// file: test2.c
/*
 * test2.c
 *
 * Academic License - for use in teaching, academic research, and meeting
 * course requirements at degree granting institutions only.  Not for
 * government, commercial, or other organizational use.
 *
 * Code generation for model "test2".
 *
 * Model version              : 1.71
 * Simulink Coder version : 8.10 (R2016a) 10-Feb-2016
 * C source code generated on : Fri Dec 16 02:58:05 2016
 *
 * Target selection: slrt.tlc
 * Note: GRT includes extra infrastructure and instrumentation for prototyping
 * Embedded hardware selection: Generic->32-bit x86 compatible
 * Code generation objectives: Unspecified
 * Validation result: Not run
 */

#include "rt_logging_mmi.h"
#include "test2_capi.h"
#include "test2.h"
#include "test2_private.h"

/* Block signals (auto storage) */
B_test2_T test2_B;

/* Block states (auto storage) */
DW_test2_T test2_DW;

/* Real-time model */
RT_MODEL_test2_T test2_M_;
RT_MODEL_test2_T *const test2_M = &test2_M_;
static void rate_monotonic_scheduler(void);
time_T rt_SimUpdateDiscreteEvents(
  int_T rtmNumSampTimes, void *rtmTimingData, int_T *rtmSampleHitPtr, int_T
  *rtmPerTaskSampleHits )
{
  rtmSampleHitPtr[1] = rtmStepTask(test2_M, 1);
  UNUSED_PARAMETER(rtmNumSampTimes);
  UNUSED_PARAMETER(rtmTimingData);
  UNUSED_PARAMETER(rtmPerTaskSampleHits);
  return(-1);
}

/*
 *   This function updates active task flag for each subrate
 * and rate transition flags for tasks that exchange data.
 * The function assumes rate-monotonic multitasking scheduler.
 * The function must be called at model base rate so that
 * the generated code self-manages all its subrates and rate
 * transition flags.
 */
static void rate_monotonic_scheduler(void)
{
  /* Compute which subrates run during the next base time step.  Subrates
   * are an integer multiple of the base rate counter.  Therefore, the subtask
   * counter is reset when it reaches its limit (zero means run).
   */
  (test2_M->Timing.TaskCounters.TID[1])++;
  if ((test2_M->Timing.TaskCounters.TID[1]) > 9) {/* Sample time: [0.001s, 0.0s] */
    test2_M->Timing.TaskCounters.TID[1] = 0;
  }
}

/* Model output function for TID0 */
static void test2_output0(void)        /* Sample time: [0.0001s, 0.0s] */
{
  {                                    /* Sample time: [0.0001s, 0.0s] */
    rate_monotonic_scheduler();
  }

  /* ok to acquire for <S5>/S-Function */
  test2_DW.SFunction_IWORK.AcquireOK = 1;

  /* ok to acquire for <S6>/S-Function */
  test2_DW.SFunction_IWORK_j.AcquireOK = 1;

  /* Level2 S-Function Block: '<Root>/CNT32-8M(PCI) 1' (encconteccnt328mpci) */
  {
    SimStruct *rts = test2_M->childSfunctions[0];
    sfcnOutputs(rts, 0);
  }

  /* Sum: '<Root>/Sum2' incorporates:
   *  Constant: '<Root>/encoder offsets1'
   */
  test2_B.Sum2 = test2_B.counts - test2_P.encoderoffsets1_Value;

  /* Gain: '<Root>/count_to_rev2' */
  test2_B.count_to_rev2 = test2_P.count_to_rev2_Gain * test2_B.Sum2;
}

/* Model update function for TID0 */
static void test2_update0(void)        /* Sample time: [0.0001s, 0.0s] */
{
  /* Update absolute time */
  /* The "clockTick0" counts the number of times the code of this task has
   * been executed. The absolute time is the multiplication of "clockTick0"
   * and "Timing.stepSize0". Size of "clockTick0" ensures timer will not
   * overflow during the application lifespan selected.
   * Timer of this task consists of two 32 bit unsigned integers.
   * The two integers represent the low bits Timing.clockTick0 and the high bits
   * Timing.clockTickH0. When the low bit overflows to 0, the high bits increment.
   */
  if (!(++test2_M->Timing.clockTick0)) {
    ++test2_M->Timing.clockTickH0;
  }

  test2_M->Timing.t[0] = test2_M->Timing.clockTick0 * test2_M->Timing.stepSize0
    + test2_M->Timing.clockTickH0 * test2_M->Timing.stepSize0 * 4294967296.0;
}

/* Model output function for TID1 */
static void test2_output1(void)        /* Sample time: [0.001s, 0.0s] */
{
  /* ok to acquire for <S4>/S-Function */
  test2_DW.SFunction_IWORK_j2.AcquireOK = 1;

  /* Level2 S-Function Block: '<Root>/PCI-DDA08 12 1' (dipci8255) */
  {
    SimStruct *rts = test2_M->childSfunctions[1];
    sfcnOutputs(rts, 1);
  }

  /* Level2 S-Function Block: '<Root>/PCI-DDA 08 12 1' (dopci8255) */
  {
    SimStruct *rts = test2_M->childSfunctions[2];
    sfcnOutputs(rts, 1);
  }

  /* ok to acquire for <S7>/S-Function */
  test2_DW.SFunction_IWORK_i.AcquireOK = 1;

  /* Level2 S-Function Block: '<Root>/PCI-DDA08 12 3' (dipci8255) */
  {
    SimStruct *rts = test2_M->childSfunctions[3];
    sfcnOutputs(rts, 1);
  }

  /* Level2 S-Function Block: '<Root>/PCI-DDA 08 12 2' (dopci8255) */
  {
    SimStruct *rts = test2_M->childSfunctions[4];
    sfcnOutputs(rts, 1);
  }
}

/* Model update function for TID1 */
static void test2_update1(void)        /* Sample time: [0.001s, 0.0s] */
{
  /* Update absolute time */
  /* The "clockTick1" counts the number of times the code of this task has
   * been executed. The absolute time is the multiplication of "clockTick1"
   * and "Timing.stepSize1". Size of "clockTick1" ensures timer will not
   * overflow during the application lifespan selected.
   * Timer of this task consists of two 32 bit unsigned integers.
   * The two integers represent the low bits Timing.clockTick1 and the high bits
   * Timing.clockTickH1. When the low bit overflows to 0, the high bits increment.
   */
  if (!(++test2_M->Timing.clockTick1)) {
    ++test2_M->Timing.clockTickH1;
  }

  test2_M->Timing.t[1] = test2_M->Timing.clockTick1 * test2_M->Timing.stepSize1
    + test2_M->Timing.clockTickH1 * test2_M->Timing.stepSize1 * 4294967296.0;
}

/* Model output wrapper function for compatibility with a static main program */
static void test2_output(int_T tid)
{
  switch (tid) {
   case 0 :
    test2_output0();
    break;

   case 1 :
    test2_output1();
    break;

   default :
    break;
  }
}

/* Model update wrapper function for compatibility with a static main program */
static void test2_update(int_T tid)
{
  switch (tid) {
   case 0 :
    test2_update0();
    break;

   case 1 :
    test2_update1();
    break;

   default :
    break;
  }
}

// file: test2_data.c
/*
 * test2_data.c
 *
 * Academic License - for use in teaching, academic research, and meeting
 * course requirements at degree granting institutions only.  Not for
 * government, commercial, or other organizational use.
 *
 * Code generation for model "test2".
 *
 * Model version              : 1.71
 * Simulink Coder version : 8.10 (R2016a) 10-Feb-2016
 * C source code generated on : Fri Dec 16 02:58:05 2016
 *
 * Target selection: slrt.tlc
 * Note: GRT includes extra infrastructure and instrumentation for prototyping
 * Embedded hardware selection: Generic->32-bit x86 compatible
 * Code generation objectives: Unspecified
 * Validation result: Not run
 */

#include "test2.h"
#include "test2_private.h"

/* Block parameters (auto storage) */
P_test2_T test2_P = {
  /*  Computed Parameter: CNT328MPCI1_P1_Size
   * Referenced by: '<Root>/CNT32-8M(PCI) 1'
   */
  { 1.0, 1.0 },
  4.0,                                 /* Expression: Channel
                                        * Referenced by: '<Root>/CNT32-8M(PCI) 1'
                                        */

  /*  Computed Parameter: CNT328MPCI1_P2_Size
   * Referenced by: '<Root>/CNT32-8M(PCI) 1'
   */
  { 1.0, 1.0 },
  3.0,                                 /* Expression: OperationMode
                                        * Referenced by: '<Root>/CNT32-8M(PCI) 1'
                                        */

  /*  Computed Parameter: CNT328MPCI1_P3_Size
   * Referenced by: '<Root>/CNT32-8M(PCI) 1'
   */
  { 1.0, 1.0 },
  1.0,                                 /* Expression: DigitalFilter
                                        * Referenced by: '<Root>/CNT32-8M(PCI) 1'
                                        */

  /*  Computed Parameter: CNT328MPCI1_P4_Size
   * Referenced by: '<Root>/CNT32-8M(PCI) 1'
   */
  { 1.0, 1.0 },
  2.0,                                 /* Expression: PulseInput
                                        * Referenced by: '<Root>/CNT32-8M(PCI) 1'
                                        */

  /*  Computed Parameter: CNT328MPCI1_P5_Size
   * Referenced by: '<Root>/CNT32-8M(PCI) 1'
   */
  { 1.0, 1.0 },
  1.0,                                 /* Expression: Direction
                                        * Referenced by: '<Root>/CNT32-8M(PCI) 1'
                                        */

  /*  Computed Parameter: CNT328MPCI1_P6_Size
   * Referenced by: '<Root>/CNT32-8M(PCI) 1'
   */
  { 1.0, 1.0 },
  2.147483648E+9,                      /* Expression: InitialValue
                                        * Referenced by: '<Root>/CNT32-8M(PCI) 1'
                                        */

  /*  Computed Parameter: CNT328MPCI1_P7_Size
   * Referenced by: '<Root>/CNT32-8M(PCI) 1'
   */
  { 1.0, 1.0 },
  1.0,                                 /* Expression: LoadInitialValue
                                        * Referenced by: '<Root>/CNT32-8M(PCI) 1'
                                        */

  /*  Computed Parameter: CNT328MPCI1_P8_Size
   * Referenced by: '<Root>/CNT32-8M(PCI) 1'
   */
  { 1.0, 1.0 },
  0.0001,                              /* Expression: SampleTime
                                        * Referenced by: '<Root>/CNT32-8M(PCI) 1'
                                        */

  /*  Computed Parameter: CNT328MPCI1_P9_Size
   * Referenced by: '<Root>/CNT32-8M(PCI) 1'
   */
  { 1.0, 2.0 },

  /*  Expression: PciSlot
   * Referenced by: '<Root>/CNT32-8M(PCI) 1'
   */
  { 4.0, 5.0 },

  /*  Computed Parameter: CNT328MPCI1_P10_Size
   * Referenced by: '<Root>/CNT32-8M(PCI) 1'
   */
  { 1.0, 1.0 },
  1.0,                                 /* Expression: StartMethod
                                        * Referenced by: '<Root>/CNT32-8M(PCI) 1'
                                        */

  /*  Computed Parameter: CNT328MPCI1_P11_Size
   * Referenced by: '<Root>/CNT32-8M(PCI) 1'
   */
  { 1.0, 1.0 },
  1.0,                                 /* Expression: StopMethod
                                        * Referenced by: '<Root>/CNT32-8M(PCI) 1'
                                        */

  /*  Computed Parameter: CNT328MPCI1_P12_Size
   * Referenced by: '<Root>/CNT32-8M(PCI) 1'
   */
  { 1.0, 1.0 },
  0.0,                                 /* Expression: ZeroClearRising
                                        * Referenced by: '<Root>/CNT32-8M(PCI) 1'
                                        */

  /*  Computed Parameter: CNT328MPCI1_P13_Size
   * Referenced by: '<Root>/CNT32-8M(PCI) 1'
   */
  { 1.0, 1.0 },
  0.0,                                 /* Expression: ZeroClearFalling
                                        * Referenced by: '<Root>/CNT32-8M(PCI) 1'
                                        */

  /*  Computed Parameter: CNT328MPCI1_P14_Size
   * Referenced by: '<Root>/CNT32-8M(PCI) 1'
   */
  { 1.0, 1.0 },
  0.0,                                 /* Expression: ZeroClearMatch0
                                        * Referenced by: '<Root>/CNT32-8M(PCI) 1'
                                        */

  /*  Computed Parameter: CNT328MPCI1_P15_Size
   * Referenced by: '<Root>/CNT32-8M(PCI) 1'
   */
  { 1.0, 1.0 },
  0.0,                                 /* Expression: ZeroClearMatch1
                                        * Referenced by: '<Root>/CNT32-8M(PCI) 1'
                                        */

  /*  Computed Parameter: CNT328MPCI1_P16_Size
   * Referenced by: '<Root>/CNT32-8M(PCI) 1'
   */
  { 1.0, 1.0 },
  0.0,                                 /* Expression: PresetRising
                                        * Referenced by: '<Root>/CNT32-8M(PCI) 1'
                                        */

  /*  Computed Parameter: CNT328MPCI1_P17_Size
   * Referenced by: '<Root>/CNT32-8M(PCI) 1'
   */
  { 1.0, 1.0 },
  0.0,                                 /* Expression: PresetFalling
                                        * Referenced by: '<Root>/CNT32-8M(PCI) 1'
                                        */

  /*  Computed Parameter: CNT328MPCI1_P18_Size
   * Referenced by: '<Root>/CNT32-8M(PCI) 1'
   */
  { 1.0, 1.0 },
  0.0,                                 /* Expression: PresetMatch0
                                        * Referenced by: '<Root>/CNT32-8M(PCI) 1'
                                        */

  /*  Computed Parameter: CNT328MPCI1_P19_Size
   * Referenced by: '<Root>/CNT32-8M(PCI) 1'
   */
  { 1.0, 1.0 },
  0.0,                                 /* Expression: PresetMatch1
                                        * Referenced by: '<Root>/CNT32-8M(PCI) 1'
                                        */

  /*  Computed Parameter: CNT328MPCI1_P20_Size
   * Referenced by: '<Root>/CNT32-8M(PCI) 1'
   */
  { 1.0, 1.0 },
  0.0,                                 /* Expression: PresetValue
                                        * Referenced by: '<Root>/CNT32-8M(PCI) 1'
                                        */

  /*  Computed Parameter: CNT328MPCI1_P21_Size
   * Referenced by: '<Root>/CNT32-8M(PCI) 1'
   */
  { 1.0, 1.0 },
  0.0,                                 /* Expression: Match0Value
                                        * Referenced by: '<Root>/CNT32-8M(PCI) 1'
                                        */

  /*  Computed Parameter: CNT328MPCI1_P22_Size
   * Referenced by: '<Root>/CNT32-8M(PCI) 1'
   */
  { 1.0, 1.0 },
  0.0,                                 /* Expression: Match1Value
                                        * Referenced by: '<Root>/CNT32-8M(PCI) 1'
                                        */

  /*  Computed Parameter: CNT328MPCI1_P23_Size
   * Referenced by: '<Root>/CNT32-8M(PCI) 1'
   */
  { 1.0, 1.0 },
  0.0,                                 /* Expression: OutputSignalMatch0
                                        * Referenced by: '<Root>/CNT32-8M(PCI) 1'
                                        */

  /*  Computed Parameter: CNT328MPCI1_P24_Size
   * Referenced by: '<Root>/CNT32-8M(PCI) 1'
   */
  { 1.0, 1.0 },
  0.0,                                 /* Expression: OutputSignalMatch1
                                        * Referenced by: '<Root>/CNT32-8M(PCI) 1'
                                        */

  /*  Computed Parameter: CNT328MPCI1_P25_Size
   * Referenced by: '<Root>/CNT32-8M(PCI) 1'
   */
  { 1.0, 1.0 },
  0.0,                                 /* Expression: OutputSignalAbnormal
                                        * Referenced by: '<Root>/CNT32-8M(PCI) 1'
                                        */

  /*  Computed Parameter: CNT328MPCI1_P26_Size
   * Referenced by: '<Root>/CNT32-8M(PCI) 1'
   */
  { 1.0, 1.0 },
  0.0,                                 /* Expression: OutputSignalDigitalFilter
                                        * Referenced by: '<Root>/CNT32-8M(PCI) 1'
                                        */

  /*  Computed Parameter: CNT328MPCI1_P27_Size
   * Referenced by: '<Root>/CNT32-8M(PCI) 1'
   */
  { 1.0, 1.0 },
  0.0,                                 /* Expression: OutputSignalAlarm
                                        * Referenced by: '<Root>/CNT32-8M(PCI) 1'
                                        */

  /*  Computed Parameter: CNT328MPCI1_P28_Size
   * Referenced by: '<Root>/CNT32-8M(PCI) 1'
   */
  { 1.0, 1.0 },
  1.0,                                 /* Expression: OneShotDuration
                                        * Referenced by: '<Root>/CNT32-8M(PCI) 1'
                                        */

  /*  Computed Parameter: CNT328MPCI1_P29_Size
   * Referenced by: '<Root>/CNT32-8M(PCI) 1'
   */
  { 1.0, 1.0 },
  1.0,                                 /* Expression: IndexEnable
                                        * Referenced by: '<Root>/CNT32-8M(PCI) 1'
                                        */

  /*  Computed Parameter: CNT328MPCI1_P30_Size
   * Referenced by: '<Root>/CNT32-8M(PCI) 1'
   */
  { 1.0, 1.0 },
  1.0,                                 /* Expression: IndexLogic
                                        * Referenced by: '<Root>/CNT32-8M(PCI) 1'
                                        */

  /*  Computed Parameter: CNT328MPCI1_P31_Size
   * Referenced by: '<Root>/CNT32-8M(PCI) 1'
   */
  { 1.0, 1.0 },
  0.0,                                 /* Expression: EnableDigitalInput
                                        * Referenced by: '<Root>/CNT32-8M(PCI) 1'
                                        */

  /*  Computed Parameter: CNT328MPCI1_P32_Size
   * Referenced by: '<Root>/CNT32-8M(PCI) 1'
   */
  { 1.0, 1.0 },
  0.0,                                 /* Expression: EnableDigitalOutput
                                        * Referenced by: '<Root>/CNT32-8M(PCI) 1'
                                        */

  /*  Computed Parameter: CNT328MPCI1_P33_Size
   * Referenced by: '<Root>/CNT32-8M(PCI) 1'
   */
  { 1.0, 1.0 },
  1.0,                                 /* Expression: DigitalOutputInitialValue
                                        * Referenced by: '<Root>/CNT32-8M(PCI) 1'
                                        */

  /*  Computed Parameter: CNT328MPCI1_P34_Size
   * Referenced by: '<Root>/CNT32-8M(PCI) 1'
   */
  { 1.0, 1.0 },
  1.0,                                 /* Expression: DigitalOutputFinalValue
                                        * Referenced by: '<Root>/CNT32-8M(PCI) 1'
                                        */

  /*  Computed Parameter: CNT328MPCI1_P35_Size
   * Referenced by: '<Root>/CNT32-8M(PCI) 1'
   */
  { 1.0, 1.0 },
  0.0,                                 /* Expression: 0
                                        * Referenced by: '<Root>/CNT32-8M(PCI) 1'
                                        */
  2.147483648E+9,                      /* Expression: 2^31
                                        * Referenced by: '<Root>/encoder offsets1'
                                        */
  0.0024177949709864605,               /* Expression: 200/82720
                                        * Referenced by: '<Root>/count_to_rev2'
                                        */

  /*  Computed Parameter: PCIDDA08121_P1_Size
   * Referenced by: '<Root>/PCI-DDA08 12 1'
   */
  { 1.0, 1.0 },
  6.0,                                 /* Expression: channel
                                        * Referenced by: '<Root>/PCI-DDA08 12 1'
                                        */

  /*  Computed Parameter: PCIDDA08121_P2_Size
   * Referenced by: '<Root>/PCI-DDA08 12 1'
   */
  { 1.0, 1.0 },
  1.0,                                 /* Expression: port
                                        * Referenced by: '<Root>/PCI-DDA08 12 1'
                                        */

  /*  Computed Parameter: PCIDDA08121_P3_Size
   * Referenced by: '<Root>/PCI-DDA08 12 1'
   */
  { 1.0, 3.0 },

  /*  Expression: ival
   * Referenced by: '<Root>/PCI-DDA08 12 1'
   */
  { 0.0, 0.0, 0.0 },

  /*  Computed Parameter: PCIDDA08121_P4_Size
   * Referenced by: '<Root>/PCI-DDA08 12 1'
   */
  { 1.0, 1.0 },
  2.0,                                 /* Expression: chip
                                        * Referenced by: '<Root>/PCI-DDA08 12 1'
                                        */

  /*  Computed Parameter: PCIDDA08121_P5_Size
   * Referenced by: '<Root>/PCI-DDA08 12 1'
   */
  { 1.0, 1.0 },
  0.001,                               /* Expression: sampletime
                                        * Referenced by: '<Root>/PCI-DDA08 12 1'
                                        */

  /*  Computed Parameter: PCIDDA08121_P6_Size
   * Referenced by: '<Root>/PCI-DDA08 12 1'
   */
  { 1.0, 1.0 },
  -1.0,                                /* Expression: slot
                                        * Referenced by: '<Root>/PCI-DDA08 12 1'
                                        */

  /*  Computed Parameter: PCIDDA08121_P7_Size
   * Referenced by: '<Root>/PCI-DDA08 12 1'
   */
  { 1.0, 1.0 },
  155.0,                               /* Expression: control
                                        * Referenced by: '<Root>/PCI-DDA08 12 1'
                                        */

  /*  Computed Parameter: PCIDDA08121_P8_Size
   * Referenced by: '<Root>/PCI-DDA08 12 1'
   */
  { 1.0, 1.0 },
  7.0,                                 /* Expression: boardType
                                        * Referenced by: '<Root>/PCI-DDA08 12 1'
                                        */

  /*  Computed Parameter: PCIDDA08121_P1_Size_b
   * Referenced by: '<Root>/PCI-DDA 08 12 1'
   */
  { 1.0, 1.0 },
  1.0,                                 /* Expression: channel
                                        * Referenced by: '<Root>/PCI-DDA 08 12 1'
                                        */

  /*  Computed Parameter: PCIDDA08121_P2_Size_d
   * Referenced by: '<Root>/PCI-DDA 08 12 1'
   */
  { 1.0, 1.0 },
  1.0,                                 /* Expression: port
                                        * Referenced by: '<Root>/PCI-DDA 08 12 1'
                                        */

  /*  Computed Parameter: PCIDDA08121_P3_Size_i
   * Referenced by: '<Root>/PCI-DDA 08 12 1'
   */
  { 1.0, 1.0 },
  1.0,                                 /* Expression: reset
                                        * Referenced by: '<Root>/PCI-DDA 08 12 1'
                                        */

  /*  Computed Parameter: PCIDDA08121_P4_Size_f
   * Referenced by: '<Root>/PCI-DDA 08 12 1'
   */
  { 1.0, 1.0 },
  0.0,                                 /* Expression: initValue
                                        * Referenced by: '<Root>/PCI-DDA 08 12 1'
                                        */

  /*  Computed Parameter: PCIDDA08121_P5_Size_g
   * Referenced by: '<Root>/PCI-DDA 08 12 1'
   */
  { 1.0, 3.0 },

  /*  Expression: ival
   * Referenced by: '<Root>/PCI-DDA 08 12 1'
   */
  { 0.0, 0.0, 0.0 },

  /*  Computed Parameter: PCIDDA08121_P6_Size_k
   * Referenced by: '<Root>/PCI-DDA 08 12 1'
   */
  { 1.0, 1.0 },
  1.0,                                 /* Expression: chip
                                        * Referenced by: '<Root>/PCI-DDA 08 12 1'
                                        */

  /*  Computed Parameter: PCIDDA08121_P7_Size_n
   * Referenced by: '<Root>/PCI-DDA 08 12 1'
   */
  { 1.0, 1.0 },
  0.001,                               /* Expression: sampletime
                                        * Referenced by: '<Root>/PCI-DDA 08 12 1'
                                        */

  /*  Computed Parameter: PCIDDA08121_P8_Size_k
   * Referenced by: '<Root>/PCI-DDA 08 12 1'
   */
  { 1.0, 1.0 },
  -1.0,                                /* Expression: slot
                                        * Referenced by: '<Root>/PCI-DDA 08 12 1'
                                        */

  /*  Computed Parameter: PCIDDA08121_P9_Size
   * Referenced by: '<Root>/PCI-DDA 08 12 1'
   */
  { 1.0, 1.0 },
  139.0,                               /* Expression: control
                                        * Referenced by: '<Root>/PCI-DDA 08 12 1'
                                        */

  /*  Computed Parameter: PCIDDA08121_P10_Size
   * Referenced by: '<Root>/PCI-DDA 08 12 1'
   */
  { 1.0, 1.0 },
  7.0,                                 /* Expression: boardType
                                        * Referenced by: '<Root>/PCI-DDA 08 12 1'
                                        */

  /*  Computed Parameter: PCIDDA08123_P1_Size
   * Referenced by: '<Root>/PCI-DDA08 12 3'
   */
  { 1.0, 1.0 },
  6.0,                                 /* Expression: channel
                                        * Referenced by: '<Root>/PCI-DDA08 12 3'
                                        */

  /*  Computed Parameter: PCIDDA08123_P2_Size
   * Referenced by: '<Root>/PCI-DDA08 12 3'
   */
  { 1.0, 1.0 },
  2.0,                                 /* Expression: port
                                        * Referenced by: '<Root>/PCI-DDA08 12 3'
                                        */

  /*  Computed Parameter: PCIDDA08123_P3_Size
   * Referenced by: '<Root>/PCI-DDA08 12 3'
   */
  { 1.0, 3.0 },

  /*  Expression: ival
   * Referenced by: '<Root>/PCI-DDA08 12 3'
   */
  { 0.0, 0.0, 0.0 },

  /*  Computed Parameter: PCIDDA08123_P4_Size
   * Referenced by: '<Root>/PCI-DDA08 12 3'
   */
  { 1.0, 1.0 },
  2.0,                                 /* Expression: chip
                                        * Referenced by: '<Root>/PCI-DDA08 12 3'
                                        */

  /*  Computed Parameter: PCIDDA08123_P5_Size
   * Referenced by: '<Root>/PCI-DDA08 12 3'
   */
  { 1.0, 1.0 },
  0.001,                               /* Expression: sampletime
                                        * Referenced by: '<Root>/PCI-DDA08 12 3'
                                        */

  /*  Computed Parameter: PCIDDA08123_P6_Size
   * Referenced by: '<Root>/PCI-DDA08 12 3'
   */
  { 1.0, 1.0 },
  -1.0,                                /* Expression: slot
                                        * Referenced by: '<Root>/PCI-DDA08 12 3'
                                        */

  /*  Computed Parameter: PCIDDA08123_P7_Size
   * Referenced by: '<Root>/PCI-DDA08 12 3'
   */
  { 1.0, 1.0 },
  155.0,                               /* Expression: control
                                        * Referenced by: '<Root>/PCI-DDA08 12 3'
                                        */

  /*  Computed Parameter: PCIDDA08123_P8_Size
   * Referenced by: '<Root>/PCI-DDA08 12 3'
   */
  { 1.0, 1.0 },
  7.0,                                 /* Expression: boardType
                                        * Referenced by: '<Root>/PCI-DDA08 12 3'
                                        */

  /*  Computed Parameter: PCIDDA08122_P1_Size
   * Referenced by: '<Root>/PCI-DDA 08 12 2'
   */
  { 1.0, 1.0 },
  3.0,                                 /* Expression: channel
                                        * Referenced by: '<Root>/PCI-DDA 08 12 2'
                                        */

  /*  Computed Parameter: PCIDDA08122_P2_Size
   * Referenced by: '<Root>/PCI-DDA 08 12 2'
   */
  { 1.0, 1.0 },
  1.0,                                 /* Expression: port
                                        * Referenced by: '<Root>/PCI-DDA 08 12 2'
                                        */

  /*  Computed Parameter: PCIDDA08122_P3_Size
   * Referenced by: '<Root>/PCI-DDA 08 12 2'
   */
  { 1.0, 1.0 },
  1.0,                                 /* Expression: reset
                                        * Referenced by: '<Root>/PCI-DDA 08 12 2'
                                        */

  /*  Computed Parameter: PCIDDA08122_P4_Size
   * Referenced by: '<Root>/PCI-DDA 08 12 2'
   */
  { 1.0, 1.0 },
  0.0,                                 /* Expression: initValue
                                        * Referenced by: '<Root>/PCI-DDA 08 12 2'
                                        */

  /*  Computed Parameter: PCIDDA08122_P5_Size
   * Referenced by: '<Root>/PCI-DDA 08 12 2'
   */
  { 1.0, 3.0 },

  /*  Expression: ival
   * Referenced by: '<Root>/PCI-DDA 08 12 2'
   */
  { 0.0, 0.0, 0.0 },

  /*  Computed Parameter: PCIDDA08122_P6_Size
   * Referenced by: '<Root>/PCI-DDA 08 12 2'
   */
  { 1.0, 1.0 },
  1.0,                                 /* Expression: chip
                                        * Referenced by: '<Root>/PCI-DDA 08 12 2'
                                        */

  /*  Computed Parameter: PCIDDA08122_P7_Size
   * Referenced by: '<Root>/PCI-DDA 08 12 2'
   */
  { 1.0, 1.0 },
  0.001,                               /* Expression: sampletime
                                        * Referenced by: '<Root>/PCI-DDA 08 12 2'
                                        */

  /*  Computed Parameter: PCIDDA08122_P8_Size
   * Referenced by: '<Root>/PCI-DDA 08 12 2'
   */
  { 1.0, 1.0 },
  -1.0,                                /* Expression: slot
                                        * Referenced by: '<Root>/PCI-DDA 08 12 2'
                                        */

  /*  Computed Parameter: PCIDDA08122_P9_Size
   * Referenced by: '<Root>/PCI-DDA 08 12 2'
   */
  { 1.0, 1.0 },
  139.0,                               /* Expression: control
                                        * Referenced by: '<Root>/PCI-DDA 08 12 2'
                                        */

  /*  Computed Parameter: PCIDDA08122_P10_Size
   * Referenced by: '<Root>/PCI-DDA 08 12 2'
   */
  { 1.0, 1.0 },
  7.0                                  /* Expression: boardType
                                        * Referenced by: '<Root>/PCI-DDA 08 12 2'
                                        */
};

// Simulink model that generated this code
simulink model "test2"  (R2016a)
settings: Solver=ode4  StartTime=0.0  StopTime=inf  RelTol=1e-3
model workspace (MAT data in the model file):
  RDTCommand : struct (value not decoded)
  java : class17 (value not decoded)
  atiData : struct (value not decoded)
  dataGramPacketRDT = [18 52 0 1 0 0 0 0]
  dpath : cell (value not decoded)
libraries: slrtlib x7, xpcmeasurementcomputinglib x5, xpcconteclib x2

== system test2 ==
  Angle : slrtlib/Displays and Logging/Scope   Commented=on  scopeno=4  scopetype=Target  autostart=on  viewmode=Numerical  formatstr='%15.6f'  grid=on  ylimits=[0,0]  nosamples=1000  noprepostsamples=0  interleave=1  triggermode=FreeRun  triggersignal=1  trigsignalfromport=off  triggerlevel=0.0  triggerslope=Either  triggerscope=1  triggersample=0  filename=data.dat  mode=Lazy  writesize=512  autorestart=off  dynamicfilemode=off  maxwritefilesize=512*1024^2
  "CNT32-8M(PCI) " : xpcconteclib/Incremental Encoder/CNT32-8M(PCI)   Commented=on  Channel=1  OperationMode=2-phase Input Synchronous Clear Multiply by 4  DigitalFilter=No filtering  PulseInput=TTL level input  Direction=Up in the clockwise direction/Down in the counterclockwise direction  InitialValue=2^31  LoadInitialValue=on  SampleTime=0.0001  PciSlot=[4 5]  StartMethod=Model Start  StopMethod=Model Terminate  ZeroClearRising=off  ZeroClearFalling=off  ZeroClearMatch0=off  ZeroClearMatch1=off  PresetRising=off  PresetFalling=off  PresetMatch0=off  PresetMatch1=off  PresetValue=0  Match0Value=0  Match1Value=0  OutputSignalMatch0=off  OutputSignalMatch1=off  OutputSignalAbnormal=off  OutputSignalDigitalFilter=off  OutputSignalAlarm=off  OneShotDuration=10 microseconds  IndexEnable=Disable  IndexLogic=Positive (Active High)  EnableDigitalInput=off  EnableDigitalOutput=off  DigitalOutputInitialValue=None  DigitalOutputFinalValue=None
  CNT32-8M(PCI) 1 : xpcconteclib/Incremental Encoder/CNT32-8M(PCI)   Channel=4  OperationMode=2-phase Input Synchronous Clear Multiply by 4  DigitalFilter=No filtering  PulseInput=TTL level input  Direction=Up in the clockwise direction/Down in the counterclockwise direction  InitialValue=2^31  LoadInitialValue=on  SampleTime=0.0001  PciSlot=[4 5]  StartMethod=Model Start  StopMethod=Model Terminate  ZeroClearRising=off  ZeroClearFalling=off  ZeroClearMatch0=off  ZeroClearMatch1=off  PresetRising=off  PresetFalling=off  PresetMatch0=off  PresetMatch1=off  PresetValue=0  Match0Value=0  Match1Value=0  OutputSignalMatch0=off  OutputSignalMatch1=off  OutputSignalAbnormal=off  OutputSignalDigitalFilter=off  OutputSignalAlarm=off  OneShotDuration=10 microseconds  IndexEnable=Disable  IndexLogic=Positive (Active High)  EnableDigitalInput=off  EnableDigitalOutput=off  DigitalOutputInitialValue=None  DigitalOutputFinalValue=None
  Constant1 : Constant  Commented=on  Value=2.5
  Constant2 : Constant  Commented=on  Value=360
  Counter : slrtlib/Displays and Logging/Scope   Commented=on  scopeno=3  scopetype=Target  autostart=on  viewmode=Numerical  formatstr='%15.6f'  grid=on  ylimits=[0,0]  nosamples=10000  noprepostsamples=0  interleave=1  triggermode=FreeRun  triggersignal=1  trigsignalfromport=off  triggerlevel=0.0  triggerslope=Either  triggerscope=1  triggersample=0  filename=data.dat  mode=Lazy  writesize=512  autorestart=off  dynamicfilemode=off  maxwritefilesize=512*1024^2
  Counter1 : slrtlib/Displays and Logging/Scope   Commented=on  scopeno=1  scopetype=Target  autostart=on  viewmode=Numerical  formatstr='%15.6f'  grid=on  ylimits=[0,0]  nosamples=10000  noprepostsamples=0  interleave=1  triggermode=FreeRun  triggersignal=1  trigsignalfromport=off  triggerlevel=0.0  triggerslope=Either  triggerscope=1  triggersample=0  filename=data.dat  mode=Lazy  writesize=512  autorestart=off  dynamicfilemode=off  maxwritefilesize=512*1024^2
  Counter2 : slrtlib/Displays and Logging/Scope   scopeno=2  scopetype=Target  autostart=on  viewmode=Numerical  formatstr='%15.6f'  grid=on  ylimits=[0,0]  nosamples=1000  noprepostsamples=0  interleave=1  triggermode=FreeRun  triggersignal=1  trigsignalfromport=off  triggerlevel=0.0  triggerslope=Either  triggerscope=1  triggersample=0  filename=data.dat  mode=Lazy  writesize=512  autorestart=off  dynamicfilemode=off  maxwritefilesize=512*1024^2
  Counter3 : slrtlib/Displays and Logging/Scope   scopeno=4  scopetype=Target  autostart=on  viewmode=Numerical  formatstr='%15.6f'  grid=on  ylimits=[0,0]  nosamples=3  noprepostsamples=0  interleave=1  triggermode=FreeRun  triggersignal=1  trigsignalfromport=off  triggerlevel=0.0  triggerslope=Either  triggerscope=1  triggersample=0  filename=data.dat  mode=Lazy  writesize=512  autorestart=off  dynamicfilemode=off  maxwritefilesize=512*1024^2
  Counter4 : slrtlib/Displays and Logging/Scope   scopeno=5  scopetype=Target  autostart=on  viewmode=Graphical rolling  formatstr='%15.6f'  grid=on  ylimits=[0,0]  nosamples=500  noprepostsamples=0  interleave=1  triggermode=FreeRun  triggersignal=1  trigsignalfromport=off  triggerlevel=0.0  triggerslope=Either  triggerscope=1  triggersample=0  filename=data.dat  mode=Lazy  writesize=512  autorestart=off  dynamicfilemode=off  maxwritefilesize=512*1024^2
  Counter5 : slrtlib/Displays and Logging/Scope   scopeno=6  scopetype=Target  autostart=on  viewmode=Numerical  formatstr='%15.6f'  grid=on  ylimits=[0,0]  nosamples=1000  noprepostsamples=0  interleave=1  triggermode=FreeRun  triggersignal=1  trigsignalfromport=off  triggerlevel=0.0  triggerslope=Either  triggerscope=1  triggersample=0  filename=data.dat  mode=Lazy  writesize=512  autorestart=off  dynamicfilemode=off  maxwritefilesize=512*1024^2
  Math Function : Math  Commented=on  Operator=mod  SaturateOnIntegerOverflow=on
  PCI-DDA 08 12 1 : xpcmeasurementcomputinglib/Digital Output/PCI-DDA08 12   channel=1  port=A  reset=[1]  initValue=[0]  chip=1  sampletime=0.001  slot=-1
  PCI-DDA 08 12 2 : xpcmeasurementcomputinglib/Digital Output/PCI-DDA08 12   channel=3  port=A  reset=[1]  initValue=[0]  chip=1  sampletime=0.001  slot=-1
  "PCI-DDA08 12 " : xpcmeasurementcomputinglib/D//A/PCI-DDA08 12   Commented=on  channel=[1 2]  range=[-10 -10]  reset=[1]  initValue=[0]  sampletime=0.001  pci_dev=-1
  PCI-DDA08 12 1 : xpcmeasurementcomputinglib/Digital Input/PCI-DDA08 12   channel=6  port=A  chip=2  sampletime=0.001  slot=-1
  PCI-DDA08 12 3 : xpcmeasurementcomputinglib/Digital Input/PCI-DDA08 12   channel=6  port=B  chip=2  sampletime=0.001  slot=-1
  Scope_angle : Scope  Commented=on
  Scope_revolution : Scope  Commented=on
  Sine Wave : Sin  Commented=on  SineType=Sample based  Amplitude=3  Frequency=0.5  Samples=10000  SampleTime=0.001
  Sum1 : Sum  Commented=on  Inputs=|+-
  Sum2 : Sum  Inputs=|+-
  count_to_rev : Gain  Commented=on  Gain=1/48
  count_to_rev1 : Gain  Commented=on  Gain=200/83289
  count_to_rev2 : Gain  Gain=200/82720
  encoder offsets : Constant  Commented=on  Value=2^31
  encoder offsets1 : Constant  Value=2^31
  inv_gear_ratio : Gain  Commented=on  Gain=1/9.7
  rev_to_degree : Gain  Commented=on  Gain=360
  wires:
  encoder offsets/1 -> Sum1/2
  "CNT32-8M(PCI) "/1 -> Sum1/1  "counts"
  inv_gear_ratio/1 -> Scope_revolution/1, rev_to_degree/1
  Sum1/1 -> Counter/1, count_to_rev1/1, count_to_rev/1
  rev_to_degree/1 -> Math Function/1
  Math Function/1 -> Angle/1, Scope_angle/1
  Constant2/1 -> Math Function/2
  count_to_rev/1 -> inv_gear_ratio/1
  count_to_rev1/1 -> Counter1/1
  PCI-DDA08 12 1/1 -> PCI-DDA 08 12 1/1, Counter2/1  "Limit Switch"
  encoder offsets1/1 -> Sum2/2
  CNT32-8M(PCI) 1/1 -> Sum2/1  "counts"
  Sum2/1 -> Counter3/1, count_to_rev2/1
  count_to_rev2/1 -> Counter4/1
  PCI-DDA08 12 3/1 -> PCI-DDA 08 12 2/1, Counter5/1  "Limit Switch"
  Constant1/1 -> "PCI-DDA08 12 "/2  "Voltage"
